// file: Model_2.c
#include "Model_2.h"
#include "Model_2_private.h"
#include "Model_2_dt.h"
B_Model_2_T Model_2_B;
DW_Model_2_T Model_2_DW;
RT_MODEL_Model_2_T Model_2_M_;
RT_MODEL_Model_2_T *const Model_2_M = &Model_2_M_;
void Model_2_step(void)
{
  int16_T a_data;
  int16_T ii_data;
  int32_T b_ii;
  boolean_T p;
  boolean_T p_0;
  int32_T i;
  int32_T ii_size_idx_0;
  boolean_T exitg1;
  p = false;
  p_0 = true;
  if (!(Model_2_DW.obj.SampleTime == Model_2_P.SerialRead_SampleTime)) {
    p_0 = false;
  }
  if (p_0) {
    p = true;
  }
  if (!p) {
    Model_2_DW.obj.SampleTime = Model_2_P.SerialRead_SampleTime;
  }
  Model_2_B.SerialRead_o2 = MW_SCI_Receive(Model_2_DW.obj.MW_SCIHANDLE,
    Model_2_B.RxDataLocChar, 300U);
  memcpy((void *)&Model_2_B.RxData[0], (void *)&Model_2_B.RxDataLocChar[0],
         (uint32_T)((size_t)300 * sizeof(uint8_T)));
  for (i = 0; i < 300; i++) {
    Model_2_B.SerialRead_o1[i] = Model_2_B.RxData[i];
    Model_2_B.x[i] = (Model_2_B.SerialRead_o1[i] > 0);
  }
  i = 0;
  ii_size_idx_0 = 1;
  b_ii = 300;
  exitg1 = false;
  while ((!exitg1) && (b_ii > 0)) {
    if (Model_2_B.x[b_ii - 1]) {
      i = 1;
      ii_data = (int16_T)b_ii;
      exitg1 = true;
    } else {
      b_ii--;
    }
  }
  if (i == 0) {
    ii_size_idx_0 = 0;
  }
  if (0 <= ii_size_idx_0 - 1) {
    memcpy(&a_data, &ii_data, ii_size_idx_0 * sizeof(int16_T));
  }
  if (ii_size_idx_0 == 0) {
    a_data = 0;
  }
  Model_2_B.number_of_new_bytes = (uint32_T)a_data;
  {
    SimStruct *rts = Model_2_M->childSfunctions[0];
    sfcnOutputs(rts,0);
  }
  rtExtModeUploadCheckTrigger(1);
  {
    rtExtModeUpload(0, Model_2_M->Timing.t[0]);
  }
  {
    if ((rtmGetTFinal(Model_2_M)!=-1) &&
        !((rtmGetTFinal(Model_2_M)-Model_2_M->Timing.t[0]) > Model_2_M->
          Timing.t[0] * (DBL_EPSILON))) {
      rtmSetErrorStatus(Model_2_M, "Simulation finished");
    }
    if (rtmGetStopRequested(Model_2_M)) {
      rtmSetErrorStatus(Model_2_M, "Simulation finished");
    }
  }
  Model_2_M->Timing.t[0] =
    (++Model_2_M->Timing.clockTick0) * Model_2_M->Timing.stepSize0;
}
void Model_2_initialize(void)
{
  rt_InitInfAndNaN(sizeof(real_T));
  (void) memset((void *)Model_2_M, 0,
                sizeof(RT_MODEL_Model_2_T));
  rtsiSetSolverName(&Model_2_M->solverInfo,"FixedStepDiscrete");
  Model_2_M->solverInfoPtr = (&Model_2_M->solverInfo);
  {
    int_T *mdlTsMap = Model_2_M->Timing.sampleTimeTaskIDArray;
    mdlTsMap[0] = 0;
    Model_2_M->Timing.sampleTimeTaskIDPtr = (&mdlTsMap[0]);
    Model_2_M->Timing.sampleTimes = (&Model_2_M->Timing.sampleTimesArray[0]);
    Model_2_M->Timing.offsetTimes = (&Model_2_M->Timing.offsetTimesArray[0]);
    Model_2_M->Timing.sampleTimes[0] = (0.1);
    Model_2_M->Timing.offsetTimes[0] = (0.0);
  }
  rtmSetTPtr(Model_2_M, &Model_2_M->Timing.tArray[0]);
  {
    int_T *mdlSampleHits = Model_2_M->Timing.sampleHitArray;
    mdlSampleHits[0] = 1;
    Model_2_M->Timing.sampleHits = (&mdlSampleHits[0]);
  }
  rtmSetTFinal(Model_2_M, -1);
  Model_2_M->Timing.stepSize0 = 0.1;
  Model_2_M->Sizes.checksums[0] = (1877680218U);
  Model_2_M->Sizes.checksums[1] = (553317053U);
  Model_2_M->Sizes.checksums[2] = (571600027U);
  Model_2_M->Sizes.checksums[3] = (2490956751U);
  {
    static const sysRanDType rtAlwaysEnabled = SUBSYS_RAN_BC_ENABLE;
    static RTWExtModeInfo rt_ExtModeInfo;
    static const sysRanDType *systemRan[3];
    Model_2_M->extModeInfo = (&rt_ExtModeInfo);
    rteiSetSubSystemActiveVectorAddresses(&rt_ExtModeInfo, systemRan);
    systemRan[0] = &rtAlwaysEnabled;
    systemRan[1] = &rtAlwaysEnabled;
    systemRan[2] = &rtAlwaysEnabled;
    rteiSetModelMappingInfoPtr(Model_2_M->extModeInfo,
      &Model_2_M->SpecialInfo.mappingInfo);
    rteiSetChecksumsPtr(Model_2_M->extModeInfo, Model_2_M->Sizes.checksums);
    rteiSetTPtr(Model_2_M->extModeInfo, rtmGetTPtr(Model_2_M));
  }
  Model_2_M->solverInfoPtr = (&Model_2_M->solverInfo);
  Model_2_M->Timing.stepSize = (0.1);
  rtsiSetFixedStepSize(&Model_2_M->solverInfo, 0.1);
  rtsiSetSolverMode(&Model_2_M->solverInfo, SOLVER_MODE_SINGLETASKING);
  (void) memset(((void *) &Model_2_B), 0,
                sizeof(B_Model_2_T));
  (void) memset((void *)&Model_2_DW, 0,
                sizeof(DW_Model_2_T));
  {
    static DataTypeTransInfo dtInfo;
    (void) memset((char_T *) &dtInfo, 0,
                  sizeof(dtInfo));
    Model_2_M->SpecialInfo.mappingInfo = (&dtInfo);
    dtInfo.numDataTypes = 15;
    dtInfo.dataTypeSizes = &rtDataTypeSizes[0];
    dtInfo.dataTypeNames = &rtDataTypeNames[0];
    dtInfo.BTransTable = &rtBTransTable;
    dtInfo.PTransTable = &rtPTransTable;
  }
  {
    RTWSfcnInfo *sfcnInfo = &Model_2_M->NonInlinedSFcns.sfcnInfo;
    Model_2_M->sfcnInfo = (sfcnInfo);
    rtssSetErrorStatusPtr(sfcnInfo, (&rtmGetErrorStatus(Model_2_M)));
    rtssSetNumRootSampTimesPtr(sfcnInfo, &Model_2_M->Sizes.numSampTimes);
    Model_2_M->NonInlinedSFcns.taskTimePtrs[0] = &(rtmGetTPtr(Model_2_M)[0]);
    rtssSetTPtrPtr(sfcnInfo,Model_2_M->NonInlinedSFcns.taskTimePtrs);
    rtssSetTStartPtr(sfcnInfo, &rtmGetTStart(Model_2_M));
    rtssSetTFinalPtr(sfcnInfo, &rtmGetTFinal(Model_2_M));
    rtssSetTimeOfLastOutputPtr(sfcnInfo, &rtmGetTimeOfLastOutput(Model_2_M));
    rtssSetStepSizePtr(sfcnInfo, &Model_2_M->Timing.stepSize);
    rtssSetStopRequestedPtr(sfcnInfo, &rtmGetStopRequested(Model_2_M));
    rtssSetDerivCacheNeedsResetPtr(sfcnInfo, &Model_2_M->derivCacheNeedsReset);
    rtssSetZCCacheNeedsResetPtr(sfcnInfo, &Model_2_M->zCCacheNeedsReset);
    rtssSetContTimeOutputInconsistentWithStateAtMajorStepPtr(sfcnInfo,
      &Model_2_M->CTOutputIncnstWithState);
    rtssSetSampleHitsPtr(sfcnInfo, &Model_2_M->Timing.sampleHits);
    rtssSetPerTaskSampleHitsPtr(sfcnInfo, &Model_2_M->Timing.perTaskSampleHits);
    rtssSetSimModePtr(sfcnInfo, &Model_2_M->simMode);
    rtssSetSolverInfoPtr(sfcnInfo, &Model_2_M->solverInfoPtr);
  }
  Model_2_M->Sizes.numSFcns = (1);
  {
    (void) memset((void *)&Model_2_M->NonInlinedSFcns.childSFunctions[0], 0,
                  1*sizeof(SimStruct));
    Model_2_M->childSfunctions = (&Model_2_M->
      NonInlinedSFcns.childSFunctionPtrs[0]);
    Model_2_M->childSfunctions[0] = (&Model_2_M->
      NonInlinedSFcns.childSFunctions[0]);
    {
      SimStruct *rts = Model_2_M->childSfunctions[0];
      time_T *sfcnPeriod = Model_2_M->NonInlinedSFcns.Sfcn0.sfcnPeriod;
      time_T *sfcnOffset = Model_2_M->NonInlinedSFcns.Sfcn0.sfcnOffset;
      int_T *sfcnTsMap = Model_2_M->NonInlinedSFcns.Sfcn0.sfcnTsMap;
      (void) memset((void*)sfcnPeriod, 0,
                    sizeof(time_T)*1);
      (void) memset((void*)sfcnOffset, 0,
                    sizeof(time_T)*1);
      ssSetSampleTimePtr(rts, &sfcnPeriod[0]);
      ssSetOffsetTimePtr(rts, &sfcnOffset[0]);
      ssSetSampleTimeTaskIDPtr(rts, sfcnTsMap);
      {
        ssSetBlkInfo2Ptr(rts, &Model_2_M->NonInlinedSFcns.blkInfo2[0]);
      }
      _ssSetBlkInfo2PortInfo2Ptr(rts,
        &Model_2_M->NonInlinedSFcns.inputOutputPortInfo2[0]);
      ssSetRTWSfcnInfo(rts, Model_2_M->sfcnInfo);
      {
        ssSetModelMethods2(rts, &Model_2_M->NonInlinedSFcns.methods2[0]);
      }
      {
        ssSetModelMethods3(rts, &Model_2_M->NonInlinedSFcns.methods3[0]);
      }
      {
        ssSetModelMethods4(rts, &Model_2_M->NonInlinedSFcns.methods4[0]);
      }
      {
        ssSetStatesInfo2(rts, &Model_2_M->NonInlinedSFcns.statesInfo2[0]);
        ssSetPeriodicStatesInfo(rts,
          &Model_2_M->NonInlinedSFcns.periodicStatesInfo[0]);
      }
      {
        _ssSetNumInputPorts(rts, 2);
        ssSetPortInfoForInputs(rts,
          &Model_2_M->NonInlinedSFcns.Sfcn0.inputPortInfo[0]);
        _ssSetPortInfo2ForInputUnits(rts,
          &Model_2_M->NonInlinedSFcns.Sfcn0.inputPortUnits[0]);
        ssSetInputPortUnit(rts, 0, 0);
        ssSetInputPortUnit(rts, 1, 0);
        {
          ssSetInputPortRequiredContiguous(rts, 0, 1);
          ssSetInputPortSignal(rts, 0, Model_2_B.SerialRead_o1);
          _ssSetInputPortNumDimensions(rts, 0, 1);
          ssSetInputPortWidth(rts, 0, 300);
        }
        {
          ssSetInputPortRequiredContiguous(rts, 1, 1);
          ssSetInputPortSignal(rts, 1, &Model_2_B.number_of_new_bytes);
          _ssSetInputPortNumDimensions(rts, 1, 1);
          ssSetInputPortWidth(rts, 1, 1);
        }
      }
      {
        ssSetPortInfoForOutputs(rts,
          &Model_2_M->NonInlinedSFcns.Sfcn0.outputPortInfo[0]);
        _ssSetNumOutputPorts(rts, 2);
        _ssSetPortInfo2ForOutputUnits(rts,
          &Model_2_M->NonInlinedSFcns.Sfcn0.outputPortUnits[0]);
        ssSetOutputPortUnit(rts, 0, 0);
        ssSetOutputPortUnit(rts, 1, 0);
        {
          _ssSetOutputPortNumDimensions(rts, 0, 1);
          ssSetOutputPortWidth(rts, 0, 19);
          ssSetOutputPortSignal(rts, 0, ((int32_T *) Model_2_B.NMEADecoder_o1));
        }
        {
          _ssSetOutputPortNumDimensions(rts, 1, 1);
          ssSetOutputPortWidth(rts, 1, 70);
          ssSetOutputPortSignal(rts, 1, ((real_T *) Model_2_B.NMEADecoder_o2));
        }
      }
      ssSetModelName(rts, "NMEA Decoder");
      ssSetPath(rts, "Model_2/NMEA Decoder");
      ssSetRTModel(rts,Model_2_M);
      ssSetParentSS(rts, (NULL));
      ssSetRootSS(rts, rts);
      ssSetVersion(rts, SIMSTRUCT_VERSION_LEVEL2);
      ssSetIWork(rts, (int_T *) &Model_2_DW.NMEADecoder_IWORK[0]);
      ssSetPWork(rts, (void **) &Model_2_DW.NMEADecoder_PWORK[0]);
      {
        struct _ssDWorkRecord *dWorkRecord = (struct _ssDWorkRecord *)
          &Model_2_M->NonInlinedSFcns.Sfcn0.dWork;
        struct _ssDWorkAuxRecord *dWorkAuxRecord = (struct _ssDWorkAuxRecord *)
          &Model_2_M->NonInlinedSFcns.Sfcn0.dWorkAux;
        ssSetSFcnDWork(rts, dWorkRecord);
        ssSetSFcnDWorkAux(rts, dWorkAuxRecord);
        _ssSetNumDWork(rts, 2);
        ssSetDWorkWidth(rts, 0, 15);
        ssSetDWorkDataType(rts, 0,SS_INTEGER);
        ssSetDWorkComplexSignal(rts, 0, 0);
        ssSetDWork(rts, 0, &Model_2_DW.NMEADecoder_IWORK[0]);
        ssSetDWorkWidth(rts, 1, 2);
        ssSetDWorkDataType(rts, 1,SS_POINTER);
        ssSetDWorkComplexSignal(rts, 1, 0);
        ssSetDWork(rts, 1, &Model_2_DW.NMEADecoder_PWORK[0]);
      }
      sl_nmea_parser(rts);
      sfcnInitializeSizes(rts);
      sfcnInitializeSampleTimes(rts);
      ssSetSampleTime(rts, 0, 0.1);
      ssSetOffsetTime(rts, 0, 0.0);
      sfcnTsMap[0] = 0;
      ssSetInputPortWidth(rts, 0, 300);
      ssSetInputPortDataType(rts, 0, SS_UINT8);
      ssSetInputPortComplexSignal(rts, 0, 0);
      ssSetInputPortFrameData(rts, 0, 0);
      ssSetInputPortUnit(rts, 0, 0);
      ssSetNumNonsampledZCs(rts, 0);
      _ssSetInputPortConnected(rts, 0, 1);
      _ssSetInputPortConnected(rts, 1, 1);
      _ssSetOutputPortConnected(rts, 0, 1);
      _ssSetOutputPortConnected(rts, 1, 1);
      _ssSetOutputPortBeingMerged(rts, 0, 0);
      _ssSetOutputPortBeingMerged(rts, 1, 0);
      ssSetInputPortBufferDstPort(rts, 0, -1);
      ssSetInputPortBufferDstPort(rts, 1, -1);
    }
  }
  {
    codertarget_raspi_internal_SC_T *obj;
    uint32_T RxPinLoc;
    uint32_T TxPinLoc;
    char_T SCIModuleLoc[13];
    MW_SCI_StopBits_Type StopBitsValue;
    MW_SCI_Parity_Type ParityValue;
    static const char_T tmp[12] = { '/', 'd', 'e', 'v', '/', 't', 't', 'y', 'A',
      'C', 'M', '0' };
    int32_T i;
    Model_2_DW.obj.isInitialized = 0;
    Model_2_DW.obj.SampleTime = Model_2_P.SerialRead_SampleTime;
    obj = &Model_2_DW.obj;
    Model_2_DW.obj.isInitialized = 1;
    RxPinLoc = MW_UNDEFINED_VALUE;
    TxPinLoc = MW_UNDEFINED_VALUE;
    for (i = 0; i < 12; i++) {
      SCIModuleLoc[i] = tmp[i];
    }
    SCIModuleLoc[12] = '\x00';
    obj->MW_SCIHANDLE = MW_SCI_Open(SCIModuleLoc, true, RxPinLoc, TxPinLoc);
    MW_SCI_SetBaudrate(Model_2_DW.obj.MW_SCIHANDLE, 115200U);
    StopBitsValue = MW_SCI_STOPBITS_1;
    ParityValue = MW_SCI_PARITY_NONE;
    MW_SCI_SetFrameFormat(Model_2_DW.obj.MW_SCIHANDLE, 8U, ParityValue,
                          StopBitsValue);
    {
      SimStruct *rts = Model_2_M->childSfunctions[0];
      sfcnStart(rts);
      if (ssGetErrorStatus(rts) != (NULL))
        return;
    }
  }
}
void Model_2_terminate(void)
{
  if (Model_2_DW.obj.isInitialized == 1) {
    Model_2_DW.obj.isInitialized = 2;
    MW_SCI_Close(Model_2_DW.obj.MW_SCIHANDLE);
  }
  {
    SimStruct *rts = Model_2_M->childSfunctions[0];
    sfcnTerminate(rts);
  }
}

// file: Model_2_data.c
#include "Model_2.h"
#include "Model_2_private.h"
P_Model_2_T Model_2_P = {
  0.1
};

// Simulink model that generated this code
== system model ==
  NMEADecoder : S-Function  FunctionName=sl_nmea_parser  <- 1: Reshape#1, 2: MATLABFunction#1
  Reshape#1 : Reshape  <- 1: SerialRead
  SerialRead : raspberrypilib/Serial Read
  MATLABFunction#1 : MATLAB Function  <- 1: SerialRead
== matlab function MATLABFunction#1 ==
function number_of_new_bytes = fcn(u)
% number_of_new_bytes = 1;
a=find(u>0,1,'last');
if isempty(a)
    a=0;
end
number_of_new_bytes = uint32(a(1));
